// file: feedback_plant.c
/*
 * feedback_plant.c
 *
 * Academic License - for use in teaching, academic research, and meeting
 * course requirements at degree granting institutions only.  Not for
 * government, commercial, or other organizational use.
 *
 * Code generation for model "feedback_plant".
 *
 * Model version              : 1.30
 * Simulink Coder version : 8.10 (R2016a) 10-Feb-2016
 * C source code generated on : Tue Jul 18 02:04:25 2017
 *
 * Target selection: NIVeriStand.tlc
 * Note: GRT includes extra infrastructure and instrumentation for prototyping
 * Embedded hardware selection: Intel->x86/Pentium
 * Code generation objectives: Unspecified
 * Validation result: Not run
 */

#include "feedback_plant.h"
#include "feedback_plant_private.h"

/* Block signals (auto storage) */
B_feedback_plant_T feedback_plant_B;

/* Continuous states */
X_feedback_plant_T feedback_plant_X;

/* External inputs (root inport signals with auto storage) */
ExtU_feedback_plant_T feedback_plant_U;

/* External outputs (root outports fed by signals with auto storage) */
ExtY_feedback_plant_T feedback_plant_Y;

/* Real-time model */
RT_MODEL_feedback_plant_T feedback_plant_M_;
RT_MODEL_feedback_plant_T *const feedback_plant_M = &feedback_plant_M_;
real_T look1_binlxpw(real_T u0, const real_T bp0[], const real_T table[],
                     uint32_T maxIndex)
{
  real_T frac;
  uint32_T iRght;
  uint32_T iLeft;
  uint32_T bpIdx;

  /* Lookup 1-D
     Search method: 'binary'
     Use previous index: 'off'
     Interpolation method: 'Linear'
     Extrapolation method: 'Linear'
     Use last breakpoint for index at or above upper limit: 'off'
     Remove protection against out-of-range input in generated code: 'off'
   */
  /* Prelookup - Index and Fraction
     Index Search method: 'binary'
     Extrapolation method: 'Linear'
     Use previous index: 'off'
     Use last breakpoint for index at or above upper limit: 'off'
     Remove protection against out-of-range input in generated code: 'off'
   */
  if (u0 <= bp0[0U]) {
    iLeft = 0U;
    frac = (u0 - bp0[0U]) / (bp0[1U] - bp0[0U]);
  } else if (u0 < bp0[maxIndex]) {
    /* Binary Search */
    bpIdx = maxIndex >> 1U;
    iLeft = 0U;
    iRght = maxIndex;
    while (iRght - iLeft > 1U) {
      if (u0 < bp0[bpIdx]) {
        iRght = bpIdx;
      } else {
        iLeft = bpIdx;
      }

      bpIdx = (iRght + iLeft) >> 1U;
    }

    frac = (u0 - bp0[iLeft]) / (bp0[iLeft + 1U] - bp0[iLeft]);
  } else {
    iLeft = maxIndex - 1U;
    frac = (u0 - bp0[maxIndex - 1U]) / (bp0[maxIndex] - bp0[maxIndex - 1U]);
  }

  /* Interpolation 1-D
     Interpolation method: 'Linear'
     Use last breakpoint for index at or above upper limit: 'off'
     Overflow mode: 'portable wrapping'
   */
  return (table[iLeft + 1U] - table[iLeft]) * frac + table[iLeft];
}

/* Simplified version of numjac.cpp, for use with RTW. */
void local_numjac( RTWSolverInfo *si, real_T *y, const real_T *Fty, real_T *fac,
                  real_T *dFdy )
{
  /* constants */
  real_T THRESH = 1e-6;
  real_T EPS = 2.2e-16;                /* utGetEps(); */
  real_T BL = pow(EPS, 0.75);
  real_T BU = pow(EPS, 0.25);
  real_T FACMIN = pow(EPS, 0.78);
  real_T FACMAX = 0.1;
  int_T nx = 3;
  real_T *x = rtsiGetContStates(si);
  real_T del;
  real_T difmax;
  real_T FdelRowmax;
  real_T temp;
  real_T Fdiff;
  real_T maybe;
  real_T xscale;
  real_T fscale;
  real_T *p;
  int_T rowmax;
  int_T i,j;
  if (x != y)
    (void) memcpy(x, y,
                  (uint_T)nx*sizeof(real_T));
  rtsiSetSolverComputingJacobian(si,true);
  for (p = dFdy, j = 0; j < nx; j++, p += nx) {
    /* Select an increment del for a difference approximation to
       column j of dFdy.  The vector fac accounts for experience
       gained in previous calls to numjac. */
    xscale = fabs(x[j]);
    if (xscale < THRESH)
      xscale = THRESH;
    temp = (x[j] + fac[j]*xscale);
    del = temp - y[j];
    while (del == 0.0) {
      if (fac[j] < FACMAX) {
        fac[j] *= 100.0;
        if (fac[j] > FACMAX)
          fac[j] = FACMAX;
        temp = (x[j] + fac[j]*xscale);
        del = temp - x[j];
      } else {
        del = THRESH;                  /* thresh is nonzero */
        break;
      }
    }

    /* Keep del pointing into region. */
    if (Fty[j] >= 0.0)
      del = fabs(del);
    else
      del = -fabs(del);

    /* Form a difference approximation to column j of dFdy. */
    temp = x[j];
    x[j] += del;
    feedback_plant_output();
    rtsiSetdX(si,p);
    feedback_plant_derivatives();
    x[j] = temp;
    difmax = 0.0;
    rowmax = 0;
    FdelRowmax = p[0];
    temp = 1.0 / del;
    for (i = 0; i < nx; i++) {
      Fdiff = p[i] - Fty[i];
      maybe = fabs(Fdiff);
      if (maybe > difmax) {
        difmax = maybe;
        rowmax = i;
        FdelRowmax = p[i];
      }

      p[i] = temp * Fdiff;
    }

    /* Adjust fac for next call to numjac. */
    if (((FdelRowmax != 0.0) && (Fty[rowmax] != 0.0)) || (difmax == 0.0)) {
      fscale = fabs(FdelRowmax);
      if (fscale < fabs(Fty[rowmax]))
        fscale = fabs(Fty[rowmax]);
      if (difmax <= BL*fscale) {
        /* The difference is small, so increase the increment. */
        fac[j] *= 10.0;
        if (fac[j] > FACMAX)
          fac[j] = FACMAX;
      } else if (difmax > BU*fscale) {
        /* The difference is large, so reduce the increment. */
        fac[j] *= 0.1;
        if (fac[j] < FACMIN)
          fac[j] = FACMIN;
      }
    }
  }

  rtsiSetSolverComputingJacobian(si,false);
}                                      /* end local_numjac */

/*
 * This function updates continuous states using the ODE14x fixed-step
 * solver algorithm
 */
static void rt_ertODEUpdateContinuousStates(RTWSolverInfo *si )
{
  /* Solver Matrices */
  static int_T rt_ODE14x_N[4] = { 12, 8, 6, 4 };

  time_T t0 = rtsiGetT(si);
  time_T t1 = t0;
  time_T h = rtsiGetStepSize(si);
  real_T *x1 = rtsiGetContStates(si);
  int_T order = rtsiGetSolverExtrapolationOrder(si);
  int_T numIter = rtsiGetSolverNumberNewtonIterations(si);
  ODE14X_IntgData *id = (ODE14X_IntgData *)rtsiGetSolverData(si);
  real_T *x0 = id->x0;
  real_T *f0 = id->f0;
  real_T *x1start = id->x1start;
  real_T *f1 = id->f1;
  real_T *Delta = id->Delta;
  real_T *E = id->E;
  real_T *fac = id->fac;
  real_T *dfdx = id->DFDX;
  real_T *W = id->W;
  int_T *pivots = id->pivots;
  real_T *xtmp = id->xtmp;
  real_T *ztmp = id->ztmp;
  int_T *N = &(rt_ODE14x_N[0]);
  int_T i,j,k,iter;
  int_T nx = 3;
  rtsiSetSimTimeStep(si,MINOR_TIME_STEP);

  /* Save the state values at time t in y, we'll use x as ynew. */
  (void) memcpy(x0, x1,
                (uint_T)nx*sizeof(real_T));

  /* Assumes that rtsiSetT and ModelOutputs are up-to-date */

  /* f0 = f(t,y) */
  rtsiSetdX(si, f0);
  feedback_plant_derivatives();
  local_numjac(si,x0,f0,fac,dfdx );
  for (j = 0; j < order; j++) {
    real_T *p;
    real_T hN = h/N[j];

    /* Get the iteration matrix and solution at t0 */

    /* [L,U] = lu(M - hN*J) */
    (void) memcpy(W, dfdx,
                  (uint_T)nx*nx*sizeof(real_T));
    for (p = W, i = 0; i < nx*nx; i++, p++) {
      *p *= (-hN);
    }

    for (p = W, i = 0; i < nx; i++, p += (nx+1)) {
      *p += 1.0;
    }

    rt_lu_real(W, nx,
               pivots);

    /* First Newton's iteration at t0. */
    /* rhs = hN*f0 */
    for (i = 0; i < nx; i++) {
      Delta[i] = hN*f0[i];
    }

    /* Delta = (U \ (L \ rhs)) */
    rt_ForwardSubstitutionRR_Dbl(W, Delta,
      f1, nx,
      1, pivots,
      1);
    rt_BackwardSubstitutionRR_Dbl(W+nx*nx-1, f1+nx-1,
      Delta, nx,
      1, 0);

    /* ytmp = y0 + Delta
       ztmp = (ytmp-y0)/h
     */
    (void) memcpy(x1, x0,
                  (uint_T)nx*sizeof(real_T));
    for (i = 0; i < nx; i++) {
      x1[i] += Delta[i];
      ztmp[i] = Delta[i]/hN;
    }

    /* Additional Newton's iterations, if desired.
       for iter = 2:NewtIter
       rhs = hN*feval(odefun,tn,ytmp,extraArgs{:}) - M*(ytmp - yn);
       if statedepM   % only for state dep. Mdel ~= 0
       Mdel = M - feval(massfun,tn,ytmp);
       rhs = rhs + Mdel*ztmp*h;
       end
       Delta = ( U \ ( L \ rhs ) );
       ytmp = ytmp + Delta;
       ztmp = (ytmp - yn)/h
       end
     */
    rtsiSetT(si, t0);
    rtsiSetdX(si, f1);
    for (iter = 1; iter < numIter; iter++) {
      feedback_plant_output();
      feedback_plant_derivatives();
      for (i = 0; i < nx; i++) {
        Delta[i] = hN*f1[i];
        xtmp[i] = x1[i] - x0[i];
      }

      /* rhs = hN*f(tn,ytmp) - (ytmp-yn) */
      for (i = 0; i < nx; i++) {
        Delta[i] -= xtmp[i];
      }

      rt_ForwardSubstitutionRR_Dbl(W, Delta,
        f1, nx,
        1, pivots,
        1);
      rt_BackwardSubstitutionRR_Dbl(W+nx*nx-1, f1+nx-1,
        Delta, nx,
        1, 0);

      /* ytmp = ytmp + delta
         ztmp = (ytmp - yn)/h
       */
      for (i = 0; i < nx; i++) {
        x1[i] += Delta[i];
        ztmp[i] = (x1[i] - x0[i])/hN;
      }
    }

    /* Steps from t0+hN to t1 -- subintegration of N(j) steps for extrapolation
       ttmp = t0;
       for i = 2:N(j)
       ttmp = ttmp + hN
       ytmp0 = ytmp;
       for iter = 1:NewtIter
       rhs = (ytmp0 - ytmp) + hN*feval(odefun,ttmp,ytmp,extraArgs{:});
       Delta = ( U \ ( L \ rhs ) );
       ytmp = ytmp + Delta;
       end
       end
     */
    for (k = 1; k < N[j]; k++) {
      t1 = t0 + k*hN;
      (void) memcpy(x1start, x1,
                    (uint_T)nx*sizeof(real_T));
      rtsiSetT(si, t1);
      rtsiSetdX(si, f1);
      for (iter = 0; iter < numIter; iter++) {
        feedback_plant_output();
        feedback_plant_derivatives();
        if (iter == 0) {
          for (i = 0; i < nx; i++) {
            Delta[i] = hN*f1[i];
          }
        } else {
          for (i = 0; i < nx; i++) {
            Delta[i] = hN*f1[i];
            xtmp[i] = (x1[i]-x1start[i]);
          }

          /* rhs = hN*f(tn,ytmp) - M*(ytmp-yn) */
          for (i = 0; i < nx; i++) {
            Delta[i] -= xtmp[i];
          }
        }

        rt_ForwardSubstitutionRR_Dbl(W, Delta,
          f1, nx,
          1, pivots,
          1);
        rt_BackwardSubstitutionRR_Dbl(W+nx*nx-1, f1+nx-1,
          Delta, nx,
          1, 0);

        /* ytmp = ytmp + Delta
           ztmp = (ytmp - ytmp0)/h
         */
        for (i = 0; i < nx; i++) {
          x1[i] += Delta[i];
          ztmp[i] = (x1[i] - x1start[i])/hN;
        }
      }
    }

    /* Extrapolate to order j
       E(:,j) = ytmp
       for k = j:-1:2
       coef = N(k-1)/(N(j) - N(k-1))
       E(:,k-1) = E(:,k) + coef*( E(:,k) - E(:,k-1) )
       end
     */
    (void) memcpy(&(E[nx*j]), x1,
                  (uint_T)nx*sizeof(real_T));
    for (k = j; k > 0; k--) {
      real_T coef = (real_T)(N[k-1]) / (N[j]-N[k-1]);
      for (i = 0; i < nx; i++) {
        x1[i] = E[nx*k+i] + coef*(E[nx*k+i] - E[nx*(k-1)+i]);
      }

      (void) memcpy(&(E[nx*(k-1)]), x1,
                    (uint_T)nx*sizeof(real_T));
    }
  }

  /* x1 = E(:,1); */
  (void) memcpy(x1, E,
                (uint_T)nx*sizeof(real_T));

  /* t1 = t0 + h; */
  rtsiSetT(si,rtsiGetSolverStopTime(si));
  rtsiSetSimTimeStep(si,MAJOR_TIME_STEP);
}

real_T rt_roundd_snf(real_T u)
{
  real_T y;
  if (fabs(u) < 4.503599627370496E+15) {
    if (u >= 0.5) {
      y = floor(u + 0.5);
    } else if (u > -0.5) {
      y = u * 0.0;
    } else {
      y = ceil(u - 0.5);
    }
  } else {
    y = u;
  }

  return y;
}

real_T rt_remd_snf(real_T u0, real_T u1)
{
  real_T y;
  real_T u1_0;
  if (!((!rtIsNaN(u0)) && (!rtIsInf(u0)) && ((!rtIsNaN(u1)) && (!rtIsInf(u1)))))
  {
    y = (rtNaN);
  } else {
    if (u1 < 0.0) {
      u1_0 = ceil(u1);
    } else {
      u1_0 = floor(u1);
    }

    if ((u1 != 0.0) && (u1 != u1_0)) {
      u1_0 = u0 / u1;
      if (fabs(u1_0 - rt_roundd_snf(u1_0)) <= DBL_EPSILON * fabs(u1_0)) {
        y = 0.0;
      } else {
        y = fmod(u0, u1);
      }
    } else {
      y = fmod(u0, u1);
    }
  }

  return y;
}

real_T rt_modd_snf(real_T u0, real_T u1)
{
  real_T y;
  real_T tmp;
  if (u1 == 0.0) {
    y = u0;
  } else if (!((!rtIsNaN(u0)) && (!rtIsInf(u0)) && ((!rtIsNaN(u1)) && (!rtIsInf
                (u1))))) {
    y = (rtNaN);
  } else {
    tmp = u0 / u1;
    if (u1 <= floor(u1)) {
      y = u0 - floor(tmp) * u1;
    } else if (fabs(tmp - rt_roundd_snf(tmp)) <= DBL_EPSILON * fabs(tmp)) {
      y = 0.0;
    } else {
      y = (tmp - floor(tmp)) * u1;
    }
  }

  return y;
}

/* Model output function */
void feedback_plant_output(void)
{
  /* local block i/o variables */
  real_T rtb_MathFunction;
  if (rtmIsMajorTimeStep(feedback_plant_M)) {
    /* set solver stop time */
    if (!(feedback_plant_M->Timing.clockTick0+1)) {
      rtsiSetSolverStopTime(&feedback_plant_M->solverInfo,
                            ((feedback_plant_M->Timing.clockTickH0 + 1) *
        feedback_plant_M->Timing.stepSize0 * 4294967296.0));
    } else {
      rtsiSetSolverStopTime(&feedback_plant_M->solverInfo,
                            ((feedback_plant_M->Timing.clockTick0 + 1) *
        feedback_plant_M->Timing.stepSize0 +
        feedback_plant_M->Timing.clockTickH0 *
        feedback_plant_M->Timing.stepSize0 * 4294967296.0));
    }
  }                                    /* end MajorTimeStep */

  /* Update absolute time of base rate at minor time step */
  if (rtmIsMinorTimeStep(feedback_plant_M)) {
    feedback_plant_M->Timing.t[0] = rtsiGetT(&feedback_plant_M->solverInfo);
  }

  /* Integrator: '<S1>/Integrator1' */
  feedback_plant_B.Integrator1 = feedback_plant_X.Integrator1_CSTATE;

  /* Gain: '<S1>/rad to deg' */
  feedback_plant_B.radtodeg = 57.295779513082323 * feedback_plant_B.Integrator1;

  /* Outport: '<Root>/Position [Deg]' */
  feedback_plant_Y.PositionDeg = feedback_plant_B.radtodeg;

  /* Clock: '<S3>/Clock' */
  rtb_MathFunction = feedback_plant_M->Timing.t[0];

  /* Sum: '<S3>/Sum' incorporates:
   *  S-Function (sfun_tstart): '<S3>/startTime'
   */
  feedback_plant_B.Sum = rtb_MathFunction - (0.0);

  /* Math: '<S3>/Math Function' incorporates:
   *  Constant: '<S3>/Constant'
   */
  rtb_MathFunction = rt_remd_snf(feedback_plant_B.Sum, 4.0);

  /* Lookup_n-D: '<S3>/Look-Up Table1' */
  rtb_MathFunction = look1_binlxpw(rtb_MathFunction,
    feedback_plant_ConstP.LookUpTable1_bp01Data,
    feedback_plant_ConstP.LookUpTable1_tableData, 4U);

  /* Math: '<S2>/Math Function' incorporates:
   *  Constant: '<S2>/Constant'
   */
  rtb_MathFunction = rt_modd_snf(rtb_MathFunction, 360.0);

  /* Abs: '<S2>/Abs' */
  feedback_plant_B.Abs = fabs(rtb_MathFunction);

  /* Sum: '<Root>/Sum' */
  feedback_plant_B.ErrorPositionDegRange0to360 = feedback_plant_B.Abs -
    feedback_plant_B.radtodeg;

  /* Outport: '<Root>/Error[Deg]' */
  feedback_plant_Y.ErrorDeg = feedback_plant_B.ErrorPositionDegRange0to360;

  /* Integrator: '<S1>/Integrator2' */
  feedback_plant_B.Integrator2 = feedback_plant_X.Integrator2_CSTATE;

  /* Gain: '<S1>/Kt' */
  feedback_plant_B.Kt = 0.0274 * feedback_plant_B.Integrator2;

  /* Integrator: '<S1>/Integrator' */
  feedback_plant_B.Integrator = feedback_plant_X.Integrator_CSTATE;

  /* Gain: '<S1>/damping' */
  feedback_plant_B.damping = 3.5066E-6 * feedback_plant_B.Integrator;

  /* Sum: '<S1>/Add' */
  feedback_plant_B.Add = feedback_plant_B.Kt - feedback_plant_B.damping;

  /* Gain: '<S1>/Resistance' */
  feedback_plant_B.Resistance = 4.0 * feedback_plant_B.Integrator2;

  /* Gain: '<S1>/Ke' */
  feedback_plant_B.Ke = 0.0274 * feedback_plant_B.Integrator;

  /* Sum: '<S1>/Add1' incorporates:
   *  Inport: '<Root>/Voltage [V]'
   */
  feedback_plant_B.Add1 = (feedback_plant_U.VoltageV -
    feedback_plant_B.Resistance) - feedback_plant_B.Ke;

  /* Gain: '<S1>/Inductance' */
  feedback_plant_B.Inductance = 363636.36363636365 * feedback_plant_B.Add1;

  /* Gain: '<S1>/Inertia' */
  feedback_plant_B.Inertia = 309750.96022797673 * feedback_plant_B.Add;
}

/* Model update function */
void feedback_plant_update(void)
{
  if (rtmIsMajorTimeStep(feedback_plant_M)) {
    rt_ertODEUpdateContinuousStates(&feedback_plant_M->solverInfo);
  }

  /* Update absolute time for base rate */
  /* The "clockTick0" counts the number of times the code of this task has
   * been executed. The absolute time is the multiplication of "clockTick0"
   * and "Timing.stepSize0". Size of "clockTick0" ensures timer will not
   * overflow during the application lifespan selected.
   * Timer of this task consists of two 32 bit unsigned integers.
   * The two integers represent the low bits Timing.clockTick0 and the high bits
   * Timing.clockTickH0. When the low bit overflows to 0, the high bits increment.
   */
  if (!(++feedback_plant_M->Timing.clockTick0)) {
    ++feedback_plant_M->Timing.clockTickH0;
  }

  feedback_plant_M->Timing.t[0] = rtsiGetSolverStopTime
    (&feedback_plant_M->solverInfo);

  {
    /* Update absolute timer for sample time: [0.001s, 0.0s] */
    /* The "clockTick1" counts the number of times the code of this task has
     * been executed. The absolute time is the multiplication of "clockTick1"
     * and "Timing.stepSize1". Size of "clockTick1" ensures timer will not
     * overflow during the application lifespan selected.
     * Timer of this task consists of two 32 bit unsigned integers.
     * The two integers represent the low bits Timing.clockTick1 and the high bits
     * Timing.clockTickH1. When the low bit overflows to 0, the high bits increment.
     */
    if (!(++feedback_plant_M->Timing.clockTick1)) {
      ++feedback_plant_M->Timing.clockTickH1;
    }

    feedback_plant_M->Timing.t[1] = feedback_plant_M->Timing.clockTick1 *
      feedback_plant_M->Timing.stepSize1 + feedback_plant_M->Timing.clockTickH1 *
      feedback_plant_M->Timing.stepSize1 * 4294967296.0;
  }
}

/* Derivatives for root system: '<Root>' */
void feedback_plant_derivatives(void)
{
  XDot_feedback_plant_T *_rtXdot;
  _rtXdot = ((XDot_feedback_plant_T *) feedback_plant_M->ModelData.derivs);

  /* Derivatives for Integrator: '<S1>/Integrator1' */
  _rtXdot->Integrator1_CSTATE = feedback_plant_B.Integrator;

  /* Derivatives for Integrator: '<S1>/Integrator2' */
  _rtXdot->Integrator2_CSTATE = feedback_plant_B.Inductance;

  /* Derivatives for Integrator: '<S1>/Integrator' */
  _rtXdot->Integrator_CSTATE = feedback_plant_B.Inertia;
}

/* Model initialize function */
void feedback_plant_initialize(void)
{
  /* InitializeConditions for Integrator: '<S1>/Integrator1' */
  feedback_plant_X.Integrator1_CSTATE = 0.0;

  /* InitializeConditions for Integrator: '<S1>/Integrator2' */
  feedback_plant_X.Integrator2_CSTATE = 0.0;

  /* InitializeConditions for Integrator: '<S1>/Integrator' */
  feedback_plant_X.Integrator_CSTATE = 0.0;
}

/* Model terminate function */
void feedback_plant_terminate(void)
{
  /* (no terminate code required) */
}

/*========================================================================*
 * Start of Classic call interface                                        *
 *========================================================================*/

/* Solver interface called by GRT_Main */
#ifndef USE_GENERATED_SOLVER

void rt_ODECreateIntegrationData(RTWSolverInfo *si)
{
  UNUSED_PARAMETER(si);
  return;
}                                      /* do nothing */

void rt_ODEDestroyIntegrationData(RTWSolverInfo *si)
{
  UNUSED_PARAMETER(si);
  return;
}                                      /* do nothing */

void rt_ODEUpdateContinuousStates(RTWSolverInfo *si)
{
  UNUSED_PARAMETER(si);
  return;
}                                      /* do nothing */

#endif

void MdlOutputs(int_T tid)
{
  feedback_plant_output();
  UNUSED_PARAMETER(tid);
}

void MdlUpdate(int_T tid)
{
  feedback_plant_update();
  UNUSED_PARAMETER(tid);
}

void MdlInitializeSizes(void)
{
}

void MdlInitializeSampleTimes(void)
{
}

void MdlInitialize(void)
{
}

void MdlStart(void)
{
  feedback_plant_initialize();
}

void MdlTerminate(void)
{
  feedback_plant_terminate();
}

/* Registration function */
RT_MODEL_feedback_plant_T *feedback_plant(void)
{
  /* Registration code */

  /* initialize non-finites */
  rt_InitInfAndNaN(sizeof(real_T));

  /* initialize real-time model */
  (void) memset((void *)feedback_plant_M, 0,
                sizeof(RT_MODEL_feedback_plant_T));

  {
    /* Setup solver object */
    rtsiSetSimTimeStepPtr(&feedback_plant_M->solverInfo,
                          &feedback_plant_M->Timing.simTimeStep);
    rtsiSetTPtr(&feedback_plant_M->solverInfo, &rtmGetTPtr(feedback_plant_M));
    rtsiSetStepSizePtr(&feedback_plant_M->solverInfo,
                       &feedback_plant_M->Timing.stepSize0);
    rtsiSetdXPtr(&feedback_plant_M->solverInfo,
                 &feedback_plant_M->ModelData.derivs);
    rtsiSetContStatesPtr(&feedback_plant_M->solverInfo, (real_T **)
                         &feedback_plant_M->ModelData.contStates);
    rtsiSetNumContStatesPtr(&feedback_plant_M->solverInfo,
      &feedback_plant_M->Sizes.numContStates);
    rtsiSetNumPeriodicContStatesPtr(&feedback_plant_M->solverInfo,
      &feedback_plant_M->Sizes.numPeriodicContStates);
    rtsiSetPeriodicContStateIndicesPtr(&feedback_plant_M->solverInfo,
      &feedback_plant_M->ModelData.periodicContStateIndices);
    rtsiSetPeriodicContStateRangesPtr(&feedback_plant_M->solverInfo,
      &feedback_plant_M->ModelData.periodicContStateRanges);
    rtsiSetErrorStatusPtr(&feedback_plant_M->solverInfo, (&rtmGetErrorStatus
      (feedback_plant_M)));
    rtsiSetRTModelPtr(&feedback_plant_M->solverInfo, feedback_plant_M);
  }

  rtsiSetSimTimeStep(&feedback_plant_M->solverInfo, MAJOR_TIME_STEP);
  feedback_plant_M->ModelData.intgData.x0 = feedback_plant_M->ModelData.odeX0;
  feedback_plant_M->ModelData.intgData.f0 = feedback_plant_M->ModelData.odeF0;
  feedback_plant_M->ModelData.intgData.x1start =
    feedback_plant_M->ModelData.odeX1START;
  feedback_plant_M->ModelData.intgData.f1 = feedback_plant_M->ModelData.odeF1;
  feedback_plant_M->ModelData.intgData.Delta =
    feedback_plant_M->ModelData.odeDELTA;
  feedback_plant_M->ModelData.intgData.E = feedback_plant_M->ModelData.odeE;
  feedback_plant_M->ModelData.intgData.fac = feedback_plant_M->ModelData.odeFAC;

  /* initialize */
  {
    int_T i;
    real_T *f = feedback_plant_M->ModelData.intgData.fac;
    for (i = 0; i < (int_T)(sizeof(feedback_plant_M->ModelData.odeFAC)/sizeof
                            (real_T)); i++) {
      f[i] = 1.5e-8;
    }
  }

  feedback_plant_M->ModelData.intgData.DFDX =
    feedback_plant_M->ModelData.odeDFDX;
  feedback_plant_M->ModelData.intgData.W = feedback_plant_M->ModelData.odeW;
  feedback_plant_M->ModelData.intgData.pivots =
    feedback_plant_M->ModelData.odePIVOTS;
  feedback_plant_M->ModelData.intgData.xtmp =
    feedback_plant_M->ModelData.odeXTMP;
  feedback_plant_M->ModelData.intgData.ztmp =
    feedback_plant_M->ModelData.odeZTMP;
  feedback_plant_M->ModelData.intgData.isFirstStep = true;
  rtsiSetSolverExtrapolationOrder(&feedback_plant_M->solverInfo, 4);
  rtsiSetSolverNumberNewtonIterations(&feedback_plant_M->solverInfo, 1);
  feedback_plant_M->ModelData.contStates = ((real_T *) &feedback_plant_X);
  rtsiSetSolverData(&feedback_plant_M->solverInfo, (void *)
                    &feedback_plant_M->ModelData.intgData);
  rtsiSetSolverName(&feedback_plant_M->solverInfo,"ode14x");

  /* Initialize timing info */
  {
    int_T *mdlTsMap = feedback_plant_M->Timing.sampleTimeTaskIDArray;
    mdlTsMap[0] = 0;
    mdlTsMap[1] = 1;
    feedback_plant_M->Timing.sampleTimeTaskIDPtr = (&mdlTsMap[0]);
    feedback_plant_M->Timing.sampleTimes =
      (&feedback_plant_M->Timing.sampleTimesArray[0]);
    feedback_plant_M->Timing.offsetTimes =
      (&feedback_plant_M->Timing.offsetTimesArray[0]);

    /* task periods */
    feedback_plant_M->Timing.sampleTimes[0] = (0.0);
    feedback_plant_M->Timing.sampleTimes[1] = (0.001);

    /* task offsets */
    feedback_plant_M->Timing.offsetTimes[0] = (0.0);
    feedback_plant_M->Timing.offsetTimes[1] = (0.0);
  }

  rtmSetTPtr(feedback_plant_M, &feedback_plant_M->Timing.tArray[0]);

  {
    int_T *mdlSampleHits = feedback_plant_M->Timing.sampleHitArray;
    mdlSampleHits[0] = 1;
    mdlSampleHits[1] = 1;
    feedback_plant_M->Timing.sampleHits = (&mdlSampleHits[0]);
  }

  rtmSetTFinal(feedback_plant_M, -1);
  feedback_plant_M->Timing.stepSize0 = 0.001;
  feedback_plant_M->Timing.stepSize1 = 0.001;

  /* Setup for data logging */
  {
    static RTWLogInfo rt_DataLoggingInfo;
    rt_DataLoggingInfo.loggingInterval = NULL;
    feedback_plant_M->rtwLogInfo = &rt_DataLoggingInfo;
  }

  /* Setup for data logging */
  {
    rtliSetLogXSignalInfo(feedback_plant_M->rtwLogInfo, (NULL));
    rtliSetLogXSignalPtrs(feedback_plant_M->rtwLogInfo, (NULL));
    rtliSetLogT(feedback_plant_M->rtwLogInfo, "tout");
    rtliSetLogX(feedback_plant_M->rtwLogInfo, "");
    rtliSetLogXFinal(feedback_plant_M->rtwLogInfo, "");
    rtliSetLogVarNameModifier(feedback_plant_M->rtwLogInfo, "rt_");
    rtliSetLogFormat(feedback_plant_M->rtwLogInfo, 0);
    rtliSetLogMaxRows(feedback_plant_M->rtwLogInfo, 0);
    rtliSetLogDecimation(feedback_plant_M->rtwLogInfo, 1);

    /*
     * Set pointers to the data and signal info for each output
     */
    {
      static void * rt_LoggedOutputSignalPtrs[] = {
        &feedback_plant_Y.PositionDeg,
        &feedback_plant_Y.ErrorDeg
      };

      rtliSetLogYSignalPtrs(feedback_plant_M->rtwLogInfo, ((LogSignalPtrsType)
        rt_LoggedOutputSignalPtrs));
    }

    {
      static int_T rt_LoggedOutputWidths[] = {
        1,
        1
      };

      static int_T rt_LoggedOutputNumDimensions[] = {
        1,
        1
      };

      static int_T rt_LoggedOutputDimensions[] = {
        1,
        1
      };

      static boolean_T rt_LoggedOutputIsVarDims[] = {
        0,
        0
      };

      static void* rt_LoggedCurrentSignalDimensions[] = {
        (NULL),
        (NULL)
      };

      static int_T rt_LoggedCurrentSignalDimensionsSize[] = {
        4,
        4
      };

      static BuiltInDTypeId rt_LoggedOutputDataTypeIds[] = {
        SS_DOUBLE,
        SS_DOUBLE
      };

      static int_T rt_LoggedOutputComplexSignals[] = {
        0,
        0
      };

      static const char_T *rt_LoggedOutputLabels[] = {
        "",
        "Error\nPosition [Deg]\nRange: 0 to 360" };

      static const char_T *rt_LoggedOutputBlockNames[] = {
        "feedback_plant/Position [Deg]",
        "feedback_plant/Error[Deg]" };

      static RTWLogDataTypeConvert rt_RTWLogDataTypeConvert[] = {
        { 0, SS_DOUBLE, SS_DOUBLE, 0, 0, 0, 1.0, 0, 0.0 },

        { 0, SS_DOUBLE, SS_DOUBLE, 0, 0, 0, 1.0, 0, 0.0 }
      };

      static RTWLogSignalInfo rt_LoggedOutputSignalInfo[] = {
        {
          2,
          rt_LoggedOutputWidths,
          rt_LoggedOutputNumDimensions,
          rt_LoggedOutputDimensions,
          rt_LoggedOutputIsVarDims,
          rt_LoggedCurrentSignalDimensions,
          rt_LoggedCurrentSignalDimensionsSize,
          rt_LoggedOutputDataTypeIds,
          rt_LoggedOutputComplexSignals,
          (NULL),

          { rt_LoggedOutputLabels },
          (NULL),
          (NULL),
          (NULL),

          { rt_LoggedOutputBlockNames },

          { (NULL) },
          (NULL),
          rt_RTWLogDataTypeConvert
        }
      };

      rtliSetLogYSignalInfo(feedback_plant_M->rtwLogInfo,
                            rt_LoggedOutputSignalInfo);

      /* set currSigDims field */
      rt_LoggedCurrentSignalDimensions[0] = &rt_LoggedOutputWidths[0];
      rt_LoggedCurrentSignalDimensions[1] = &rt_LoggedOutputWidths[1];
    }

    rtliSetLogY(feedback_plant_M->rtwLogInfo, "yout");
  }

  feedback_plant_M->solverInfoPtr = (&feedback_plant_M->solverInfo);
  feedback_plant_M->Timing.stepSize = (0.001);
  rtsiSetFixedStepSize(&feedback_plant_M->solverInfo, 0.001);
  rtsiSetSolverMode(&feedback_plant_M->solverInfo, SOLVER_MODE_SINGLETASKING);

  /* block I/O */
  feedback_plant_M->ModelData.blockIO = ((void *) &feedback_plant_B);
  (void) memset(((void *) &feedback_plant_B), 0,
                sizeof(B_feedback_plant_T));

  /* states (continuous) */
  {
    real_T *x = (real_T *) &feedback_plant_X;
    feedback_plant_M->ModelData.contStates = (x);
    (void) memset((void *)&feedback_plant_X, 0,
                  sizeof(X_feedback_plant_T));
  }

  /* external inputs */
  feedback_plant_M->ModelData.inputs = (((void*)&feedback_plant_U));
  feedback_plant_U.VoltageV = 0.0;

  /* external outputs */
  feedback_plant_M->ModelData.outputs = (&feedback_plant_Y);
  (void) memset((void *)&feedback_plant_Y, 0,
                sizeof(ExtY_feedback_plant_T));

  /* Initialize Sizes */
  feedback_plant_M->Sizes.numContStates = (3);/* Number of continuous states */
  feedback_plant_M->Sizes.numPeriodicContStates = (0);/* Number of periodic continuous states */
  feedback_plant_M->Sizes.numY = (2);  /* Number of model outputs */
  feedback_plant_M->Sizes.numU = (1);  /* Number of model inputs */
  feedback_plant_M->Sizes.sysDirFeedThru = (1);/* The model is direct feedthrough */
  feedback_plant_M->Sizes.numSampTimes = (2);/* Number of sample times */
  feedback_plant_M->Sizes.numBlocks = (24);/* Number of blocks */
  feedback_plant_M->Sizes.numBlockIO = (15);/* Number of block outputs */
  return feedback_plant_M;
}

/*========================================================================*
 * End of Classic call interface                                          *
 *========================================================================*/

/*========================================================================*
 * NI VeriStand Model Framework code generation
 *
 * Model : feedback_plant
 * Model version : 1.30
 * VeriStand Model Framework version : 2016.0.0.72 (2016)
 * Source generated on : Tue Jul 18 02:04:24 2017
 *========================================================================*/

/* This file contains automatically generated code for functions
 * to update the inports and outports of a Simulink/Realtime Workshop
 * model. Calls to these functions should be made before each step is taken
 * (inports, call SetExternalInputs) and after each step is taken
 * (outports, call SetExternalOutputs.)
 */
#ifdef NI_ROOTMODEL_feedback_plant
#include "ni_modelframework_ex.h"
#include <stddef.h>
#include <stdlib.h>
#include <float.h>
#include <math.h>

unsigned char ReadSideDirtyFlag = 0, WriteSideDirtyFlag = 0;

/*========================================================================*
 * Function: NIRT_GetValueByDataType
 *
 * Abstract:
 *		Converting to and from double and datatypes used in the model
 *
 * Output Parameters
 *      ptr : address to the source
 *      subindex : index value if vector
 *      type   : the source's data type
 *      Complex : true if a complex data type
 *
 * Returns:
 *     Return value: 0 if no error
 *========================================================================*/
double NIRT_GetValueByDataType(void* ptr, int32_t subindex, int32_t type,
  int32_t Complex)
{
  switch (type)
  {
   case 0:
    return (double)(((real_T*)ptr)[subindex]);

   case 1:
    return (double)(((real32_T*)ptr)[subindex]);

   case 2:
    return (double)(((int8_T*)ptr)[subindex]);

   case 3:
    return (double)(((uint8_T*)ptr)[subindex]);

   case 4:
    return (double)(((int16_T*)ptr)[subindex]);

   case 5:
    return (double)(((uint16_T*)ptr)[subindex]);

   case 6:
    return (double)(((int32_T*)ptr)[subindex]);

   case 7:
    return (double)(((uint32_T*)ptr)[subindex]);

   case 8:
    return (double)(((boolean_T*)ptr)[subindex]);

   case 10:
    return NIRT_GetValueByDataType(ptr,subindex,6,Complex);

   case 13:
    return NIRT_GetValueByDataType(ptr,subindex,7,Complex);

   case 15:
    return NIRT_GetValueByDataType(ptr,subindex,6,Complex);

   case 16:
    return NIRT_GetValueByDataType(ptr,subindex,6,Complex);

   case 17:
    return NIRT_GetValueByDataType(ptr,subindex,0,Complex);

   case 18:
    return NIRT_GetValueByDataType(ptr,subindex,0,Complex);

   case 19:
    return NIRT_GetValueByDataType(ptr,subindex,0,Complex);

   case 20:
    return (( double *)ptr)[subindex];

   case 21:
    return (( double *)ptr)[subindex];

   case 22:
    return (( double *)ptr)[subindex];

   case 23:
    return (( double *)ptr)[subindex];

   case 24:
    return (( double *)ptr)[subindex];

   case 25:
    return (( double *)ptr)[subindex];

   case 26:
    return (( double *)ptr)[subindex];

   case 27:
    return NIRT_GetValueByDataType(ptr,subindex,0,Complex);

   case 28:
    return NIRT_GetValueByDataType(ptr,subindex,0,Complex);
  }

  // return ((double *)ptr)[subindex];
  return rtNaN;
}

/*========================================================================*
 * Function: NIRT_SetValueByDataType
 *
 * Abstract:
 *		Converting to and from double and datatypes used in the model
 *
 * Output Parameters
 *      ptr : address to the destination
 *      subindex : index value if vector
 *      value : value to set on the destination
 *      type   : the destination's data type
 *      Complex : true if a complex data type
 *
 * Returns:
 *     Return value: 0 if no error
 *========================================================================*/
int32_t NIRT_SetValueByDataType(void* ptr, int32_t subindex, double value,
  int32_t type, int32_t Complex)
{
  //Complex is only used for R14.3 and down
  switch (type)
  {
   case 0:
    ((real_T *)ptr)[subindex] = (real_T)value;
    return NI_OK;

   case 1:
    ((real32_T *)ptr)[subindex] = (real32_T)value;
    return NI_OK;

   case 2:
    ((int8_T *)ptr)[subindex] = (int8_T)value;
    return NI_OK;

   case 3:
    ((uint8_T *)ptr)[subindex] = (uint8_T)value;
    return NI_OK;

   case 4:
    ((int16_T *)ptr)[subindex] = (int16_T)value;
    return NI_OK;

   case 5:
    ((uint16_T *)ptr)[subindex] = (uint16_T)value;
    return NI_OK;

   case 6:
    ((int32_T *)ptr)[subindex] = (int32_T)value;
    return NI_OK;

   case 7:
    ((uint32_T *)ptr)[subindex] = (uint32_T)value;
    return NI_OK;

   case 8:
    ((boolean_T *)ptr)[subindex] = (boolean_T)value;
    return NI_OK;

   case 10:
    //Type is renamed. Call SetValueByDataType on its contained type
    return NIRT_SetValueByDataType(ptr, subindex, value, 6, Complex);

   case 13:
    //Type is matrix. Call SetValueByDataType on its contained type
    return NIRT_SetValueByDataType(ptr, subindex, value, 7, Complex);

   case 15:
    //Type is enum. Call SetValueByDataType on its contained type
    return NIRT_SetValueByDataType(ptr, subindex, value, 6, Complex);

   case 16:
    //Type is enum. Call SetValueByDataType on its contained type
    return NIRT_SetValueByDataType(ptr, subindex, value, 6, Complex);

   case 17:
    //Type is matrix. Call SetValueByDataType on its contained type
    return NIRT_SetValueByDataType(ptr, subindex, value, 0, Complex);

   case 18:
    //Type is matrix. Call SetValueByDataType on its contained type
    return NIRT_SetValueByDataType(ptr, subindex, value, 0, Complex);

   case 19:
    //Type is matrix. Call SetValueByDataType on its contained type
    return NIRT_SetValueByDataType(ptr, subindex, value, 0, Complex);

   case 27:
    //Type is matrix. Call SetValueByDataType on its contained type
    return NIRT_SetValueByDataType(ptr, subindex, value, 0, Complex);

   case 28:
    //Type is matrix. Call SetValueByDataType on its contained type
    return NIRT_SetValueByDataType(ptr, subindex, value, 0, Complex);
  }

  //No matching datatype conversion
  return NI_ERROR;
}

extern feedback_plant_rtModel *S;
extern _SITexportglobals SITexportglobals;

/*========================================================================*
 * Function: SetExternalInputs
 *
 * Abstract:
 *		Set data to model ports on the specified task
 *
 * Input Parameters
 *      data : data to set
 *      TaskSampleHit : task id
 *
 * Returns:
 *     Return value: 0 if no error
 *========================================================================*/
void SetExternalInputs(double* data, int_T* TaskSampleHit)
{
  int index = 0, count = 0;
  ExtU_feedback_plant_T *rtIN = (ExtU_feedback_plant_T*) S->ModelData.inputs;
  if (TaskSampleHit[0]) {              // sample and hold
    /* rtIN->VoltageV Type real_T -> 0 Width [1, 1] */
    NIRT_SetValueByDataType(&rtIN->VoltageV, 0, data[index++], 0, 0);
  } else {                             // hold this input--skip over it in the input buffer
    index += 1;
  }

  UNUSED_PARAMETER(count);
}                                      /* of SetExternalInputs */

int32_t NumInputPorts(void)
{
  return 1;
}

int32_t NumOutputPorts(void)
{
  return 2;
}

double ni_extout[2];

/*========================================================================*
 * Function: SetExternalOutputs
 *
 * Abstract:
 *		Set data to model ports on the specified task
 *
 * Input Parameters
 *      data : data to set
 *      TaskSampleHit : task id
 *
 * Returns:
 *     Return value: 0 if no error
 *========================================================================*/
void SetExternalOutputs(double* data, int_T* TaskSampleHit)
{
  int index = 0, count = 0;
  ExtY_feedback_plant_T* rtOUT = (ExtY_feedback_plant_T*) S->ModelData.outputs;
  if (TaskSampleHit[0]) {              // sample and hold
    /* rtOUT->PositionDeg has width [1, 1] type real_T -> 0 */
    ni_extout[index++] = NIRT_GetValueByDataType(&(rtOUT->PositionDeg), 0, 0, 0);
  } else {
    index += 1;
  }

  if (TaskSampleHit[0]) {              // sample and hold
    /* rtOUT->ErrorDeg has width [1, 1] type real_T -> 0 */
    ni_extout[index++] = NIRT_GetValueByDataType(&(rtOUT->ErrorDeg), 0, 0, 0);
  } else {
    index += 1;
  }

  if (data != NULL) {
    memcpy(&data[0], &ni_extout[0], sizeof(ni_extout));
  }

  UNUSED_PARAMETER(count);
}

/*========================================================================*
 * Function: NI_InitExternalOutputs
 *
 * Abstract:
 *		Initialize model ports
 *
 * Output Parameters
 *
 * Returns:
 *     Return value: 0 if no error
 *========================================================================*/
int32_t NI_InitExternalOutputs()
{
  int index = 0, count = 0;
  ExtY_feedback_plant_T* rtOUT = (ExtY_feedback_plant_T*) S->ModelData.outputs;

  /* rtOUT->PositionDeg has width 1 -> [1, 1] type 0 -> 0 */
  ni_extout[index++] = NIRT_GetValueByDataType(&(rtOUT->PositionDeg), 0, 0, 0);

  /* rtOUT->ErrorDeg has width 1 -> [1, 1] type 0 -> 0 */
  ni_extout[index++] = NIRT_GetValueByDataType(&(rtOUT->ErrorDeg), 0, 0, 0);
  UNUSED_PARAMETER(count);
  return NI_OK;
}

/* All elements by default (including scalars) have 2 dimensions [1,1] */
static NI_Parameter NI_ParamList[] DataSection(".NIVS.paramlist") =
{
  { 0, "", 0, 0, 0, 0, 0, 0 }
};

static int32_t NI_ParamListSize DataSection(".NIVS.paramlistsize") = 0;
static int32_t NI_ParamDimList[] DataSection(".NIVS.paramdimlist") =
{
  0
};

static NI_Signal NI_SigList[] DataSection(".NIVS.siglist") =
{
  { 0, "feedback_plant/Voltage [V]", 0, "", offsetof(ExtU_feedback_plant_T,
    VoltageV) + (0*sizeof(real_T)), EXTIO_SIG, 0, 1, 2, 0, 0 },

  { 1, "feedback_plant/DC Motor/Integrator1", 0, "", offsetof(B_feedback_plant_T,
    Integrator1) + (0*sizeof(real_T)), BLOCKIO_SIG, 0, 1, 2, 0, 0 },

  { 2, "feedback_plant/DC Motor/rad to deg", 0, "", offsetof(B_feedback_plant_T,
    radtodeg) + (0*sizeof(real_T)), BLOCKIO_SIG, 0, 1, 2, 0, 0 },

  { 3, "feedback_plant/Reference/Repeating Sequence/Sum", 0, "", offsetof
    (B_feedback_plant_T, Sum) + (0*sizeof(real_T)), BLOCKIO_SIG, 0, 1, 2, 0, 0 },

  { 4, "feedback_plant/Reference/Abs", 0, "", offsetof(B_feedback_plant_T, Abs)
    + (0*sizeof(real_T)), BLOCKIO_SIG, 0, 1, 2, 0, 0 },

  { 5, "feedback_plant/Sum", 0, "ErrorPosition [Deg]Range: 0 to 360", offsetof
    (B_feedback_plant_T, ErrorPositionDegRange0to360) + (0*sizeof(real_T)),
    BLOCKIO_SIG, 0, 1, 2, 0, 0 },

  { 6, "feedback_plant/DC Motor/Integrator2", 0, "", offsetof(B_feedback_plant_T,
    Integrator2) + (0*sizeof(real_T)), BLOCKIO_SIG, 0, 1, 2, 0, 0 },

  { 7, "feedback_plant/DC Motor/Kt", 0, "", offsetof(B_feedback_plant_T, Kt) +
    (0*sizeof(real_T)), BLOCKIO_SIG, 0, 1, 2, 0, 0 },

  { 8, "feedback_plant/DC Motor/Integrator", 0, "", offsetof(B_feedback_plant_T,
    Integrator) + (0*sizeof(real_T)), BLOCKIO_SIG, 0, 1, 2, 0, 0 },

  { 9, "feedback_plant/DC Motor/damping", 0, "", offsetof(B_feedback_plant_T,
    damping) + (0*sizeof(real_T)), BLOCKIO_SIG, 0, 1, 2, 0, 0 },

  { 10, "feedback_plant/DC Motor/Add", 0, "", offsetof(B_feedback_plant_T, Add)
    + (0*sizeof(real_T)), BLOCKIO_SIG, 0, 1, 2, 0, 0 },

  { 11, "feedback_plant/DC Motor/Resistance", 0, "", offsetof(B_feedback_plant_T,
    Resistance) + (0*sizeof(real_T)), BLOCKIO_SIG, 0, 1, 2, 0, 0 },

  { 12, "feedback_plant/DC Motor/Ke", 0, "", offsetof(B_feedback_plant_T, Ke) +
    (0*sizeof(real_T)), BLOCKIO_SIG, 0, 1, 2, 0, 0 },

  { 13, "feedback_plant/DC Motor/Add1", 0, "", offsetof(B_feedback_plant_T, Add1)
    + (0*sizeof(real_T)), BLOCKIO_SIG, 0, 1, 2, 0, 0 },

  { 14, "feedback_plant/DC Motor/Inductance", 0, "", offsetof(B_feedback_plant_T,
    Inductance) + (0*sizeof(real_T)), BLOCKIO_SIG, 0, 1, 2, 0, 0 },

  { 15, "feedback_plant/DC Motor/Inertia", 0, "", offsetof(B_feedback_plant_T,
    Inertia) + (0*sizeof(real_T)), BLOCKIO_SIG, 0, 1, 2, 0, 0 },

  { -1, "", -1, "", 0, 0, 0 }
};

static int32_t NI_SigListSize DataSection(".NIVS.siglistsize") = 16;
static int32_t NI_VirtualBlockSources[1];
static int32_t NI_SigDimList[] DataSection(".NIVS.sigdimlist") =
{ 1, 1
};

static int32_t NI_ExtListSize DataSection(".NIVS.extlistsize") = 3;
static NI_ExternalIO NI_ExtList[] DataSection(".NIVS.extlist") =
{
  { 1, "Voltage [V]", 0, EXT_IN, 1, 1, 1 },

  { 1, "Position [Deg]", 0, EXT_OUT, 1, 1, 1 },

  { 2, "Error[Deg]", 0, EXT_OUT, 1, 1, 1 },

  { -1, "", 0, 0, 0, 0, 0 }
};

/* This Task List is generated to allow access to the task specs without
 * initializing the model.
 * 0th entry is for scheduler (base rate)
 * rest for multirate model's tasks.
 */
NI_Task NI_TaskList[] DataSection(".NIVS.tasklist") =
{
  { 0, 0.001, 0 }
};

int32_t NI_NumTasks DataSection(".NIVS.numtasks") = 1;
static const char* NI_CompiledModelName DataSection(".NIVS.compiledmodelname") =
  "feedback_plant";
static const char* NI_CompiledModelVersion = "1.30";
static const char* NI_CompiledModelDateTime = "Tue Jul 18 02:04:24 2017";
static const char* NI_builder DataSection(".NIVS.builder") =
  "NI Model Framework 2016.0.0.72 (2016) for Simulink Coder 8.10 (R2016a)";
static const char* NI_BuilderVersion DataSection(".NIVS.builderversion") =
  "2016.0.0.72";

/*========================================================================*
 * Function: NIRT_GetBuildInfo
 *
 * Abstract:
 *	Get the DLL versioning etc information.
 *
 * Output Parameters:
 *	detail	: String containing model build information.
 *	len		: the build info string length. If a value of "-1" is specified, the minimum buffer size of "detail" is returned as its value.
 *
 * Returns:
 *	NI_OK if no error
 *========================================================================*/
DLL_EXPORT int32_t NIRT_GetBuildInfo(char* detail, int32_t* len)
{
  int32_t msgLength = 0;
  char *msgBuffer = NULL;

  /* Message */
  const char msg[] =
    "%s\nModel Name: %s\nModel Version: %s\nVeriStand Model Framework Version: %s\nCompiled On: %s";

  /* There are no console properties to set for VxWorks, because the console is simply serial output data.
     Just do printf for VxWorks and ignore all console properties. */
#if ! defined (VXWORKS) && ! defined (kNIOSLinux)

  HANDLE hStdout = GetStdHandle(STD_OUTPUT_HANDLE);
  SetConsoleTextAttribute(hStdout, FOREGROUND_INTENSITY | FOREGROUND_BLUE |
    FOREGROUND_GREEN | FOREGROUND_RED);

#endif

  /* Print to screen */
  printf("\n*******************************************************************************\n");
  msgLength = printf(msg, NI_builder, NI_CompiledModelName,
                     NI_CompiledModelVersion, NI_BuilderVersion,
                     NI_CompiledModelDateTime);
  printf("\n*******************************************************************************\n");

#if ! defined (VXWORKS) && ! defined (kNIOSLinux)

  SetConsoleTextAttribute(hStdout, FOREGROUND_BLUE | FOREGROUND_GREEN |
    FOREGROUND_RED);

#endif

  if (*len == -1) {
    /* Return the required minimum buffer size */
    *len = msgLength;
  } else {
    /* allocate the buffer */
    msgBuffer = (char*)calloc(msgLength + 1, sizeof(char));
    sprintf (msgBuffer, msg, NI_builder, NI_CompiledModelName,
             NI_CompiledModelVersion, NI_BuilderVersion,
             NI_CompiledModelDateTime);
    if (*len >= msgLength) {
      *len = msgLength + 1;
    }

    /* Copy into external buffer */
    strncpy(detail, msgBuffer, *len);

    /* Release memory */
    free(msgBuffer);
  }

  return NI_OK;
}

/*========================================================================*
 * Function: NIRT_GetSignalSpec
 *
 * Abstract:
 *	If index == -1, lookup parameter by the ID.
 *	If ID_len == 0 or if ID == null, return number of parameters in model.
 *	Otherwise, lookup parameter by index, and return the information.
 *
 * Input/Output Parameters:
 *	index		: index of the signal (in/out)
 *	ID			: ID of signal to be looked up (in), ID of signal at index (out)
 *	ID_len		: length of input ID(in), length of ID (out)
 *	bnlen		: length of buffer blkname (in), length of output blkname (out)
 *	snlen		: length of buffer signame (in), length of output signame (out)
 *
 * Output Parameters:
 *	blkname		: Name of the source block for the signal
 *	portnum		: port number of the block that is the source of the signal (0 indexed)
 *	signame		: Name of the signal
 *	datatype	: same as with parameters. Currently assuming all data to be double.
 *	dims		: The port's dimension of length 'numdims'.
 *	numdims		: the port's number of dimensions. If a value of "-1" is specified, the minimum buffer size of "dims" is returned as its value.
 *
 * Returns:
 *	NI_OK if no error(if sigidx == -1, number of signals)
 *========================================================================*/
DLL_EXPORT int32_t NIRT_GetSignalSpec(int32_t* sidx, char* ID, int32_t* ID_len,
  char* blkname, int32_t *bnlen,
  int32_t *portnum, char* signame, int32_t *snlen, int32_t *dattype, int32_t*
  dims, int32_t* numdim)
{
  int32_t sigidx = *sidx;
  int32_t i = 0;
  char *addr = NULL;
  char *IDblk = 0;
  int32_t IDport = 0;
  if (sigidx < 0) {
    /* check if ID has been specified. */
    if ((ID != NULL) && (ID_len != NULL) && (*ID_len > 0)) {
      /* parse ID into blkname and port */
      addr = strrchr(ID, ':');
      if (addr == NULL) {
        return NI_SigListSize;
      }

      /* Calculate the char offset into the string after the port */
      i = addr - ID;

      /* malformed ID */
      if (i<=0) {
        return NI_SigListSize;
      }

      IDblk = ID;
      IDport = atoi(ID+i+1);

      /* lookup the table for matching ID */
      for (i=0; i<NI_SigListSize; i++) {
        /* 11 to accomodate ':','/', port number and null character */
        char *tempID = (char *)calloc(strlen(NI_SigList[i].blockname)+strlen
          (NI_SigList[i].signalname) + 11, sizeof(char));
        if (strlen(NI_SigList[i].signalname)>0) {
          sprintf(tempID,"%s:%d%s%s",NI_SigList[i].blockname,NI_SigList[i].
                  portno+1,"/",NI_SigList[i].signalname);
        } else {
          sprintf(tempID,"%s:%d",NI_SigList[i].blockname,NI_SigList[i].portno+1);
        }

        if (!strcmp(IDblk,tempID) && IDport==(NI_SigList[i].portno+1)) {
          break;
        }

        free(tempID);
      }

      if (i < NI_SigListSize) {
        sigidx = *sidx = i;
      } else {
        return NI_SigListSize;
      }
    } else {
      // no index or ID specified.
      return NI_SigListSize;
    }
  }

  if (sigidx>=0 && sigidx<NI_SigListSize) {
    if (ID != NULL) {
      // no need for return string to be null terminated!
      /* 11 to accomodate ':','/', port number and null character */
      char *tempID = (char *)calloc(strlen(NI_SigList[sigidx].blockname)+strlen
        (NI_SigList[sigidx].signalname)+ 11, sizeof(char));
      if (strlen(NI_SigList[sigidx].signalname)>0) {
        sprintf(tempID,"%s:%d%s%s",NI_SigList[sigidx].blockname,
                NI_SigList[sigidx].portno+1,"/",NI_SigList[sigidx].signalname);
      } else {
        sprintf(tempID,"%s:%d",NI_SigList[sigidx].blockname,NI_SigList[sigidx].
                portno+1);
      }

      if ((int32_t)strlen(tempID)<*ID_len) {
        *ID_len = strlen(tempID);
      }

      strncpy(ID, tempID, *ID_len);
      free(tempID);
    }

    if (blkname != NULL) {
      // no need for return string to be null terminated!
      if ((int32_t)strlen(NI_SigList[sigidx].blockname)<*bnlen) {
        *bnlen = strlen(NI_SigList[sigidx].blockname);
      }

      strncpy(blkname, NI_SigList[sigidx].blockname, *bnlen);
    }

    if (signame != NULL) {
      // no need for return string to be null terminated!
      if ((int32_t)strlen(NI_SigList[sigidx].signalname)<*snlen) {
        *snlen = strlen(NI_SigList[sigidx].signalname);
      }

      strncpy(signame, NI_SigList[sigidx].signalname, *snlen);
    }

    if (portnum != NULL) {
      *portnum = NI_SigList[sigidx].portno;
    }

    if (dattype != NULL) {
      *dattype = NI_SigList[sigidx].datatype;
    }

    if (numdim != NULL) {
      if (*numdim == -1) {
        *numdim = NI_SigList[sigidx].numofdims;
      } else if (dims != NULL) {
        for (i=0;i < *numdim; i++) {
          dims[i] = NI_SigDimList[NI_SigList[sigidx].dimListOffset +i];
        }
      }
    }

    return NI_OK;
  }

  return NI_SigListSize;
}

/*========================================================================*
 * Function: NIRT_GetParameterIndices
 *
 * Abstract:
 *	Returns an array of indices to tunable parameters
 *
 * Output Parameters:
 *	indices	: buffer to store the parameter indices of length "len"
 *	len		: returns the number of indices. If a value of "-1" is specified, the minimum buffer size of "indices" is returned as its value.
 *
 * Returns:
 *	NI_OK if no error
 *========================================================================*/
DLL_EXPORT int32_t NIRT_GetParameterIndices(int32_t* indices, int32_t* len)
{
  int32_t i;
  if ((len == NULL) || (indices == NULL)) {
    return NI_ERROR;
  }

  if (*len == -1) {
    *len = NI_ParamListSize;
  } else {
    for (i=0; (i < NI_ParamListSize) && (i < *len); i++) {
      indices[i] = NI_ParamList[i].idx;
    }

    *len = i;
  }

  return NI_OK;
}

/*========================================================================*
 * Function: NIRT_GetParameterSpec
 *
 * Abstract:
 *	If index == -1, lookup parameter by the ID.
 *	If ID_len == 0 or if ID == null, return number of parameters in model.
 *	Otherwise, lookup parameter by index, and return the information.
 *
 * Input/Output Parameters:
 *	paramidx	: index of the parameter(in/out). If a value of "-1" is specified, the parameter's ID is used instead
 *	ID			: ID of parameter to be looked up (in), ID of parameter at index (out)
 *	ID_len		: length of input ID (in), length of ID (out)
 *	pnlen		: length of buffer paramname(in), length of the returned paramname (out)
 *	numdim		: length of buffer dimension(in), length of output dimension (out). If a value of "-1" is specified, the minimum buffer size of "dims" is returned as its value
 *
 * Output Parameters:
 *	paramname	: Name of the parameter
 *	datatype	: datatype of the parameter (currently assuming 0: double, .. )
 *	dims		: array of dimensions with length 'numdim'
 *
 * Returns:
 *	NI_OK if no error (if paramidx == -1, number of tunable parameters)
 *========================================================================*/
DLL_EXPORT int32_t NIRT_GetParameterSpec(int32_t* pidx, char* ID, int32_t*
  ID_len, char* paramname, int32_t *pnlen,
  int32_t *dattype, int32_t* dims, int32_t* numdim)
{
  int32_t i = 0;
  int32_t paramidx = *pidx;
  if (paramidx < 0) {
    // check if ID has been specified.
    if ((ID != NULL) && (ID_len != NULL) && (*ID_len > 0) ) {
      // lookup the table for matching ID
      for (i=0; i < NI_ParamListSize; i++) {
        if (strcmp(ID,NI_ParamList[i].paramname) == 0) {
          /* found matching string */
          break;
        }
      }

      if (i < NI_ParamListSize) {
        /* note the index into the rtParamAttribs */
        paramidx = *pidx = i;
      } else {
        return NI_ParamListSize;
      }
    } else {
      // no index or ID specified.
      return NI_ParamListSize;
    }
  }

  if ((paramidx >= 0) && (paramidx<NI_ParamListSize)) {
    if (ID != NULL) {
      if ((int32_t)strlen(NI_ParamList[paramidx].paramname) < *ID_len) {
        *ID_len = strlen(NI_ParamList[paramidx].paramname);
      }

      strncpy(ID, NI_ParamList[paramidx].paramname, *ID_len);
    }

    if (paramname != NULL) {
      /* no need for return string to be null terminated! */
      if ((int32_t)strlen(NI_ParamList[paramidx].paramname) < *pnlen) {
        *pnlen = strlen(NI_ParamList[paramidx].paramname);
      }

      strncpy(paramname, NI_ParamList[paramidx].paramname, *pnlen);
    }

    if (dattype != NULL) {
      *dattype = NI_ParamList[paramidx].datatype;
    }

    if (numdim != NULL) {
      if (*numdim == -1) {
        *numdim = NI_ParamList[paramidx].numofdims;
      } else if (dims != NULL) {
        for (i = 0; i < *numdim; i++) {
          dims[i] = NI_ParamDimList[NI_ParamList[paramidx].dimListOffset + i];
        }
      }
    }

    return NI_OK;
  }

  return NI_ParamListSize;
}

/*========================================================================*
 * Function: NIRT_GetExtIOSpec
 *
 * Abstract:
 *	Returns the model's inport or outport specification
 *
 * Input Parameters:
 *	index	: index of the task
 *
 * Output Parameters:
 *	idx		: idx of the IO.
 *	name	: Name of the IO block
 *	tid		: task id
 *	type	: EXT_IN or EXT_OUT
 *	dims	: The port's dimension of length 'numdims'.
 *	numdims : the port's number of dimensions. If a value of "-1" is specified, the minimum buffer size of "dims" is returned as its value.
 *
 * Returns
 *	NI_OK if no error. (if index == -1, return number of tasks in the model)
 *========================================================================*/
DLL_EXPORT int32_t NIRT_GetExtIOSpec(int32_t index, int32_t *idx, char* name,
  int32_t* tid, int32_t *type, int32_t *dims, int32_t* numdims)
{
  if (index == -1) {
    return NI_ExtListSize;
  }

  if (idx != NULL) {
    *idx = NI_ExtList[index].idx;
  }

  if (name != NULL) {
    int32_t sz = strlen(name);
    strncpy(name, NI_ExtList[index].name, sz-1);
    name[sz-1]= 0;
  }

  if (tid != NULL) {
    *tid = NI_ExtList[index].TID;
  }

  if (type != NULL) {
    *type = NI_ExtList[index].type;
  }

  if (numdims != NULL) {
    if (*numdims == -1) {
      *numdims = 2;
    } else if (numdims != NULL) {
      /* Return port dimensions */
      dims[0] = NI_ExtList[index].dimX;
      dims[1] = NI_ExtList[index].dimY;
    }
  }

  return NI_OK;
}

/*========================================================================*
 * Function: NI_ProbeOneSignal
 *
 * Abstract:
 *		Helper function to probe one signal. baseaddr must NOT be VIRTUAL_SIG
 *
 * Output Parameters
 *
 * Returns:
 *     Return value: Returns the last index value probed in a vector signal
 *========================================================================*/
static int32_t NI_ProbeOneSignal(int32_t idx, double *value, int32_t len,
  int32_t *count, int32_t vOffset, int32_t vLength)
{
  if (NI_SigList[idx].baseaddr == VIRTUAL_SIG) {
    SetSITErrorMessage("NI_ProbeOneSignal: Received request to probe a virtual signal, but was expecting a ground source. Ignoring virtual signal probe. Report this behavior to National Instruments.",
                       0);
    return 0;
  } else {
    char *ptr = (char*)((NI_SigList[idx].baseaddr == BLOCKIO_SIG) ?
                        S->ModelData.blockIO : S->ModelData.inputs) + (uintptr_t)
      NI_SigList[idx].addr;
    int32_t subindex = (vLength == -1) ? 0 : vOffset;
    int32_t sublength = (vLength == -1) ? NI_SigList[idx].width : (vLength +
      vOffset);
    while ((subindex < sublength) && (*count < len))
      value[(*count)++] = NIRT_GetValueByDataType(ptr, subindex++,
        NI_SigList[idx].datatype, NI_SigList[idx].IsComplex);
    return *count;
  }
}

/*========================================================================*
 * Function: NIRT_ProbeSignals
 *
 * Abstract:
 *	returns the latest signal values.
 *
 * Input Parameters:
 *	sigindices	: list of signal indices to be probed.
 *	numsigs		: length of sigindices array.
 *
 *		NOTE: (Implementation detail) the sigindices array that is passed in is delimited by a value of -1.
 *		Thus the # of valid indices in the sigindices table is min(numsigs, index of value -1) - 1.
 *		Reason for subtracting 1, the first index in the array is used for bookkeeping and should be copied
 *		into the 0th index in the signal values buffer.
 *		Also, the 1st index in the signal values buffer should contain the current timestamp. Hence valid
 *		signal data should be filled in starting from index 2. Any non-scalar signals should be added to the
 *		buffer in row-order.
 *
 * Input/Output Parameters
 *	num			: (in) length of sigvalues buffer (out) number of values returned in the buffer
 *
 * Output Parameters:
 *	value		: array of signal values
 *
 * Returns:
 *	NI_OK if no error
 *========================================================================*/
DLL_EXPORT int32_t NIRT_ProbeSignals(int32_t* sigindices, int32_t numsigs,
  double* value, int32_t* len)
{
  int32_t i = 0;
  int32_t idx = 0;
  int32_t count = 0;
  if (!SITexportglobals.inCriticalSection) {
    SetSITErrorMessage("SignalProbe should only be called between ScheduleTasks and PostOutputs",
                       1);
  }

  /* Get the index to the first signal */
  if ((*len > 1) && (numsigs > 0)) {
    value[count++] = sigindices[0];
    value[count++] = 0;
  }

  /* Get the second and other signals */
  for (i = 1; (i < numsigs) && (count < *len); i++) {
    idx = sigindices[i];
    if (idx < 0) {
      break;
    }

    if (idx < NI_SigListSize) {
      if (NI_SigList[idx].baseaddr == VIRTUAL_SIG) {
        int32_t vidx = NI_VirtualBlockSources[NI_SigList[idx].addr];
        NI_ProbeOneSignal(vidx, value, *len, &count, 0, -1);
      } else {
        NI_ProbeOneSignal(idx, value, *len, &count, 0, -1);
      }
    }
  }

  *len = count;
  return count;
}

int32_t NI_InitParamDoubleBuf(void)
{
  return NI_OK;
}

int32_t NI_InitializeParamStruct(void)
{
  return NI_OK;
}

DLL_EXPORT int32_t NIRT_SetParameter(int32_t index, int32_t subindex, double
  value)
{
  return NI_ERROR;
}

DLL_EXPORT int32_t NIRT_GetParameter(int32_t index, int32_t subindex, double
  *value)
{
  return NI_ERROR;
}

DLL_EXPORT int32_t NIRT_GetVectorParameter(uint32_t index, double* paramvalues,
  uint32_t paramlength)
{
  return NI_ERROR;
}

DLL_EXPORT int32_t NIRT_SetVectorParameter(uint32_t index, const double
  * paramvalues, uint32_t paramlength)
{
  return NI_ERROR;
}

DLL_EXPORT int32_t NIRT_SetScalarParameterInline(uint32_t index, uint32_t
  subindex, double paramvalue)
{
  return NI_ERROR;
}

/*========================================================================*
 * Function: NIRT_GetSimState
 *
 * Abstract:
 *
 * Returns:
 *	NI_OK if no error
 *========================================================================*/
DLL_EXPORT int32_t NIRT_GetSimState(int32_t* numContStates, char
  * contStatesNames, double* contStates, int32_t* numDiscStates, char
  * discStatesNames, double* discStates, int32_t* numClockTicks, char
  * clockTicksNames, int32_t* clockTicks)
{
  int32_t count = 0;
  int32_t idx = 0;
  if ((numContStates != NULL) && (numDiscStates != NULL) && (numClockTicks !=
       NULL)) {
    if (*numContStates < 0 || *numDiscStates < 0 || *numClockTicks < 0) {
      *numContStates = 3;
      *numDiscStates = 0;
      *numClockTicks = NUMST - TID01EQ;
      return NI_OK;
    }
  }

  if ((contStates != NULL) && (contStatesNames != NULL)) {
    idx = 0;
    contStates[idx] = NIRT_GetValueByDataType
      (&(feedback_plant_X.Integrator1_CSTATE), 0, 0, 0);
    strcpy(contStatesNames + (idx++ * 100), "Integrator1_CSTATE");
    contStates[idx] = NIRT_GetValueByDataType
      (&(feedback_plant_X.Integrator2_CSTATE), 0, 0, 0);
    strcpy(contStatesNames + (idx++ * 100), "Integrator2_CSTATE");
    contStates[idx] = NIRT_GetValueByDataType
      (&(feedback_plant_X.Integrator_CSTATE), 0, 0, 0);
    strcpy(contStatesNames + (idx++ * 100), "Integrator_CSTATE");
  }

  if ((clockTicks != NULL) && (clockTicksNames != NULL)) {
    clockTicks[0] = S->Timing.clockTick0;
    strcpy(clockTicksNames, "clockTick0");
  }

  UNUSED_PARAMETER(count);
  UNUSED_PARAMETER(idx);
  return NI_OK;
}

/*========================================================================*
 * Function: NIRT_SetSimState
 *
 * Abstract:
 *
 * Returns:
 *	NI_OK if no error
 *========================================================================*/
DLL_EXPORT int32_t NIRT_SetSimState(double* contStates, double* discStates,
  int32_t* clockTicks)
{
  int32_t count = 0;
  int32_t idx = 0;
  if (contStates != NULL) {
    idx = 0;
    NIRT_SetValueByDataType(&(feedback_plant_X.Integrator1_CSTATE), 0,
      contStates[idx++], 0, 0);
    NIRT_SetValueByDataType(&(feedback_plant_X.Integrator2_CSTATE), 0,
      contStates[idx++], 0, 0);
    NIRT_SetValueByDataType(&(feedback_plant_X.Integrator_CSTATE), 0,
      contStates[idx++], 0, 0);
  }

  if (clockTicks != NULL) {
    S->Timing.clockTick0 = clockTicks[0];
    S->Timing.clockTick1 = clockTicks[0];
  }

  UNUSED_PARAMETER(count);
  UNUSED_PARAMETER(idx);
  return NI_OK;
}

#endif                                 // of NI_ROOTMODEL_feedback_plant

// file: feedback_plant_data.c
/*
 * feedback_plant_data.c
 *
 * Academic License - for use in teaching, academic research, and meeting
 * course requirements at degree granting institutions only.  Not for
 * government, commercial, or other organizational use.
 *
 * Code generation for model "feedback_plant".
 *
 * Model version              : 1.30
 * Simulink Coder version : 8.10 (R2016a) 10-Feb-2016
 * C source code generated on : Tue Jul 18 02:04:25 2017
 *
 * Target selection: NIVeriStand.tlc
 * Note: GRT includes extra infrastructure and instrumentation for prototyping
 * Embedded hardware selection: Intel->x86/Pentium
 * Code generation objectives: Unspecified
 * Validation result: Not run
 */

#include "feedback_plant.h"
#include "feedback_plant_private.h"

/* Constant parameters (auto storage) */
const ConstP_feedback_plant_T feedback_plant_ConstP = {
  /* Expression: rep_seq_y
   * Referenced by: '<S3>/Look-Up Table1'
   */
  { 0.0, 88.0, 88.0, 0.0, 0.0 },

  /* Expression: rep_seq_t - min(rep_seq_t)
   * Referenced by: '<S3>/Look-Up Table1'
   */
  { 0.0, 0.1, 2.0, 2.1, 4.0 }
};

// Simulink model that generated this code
simulink model "feedback_plant"  (R2016a)
settings: Solver=ode14x  StartTime=0.0  StopTime=inf  FixedStep=1e-3  MaxStep=0.1  RelTol=1e-3
undefined symbols (not defined in the file): b, J, K, L, R
libraries: simulink x1

== system feedback_plant ==
  note: Reference
      | Position [Deg]
      | Range: 0 to 360
  note: Copyright 2012-2015 The MathWorks, Inc.
  note: DC Motor
      | The model simulates a DC motor, receiving as input the control voltage, and producing the position in degree of the DC motor shaft.
  Voltage [V] : Inport
  DC Motor : Subsystem
  Reference : Subsystem
  Sum : Sum  Inputs=|+-
  Position [Deg] : Outport
  Error[Deg] : Outport  Port=2
  wires:
  Voltage [V]/1 -> DC Motor/1(Voltage)
  Reference/1(Ref [Deg]) -> Sum/1
  Sum/1 -> Error[Deg]/1  "Error Position [Deg] Range: 0 to 360"
  DC Motor/1(Position) -> Sum/2, Position [Deg]/1

== system feedback_plant/DC Motor ==
  note: i
  note: d/dt(theta)
  note: d2/dt2(theta)
  note: d/dt(i)
  note: theta
  Voltage : Inport
  Add : Sum  Inputs=+-
  Add1 : Sum  Inputs=-+-
  Inductance : Gain  Gain=1/L
  Inertia : Gain  Gain=1/J
  Integrator : Integrator
  Integrator1 : Integrator
  Integrator2 : Integrator
  Ke : Gain  Gain=K
  Kt : Gain  Gain=K
  Resistance : Gain  Gain=R
  damping : Gain  Gain=b
  rad to deg : Gain  Gain=180/pi
  Position : Outport
  wires:
  Inductance/1 -> Integrator2/1
  Integrator/1 -> Integrator1/1, damping/1, Ke/1
  Integrator1/1 -> rad to deg/1
  Inertia/1 -> Integrator/1
  Integrator2/1 -> Kt/1, Resistance/1
  Add/1 -> Inertia/1
  Add1/1 -> Inductance/1
  Kt/1 -> Add/1
  damping/1 -> Add/2
  Ke/1 -> Add1/3
  Resistance/1 -> Add1/1
  Voltage/1 -> Add1/2
  rad to deg/1 -> Position/1

== system feedback_plant/Reference ==
  note: Reference input model
      | Provide the reference for the DC motor shaft (in degree) to be followed by the controller.
  Abs : Abs
  Constant : Constant  Value=360
  Math Function : Math  Operator=mod  SaturateOnIntegerOverflow=on
  Repeating Sequence : simulink/Sources/Repeating Sequence  rep_seq_t=[0 0.1 2 2.1 4]  rep_seq_y=[0 88 88 0 0].'
  Ref [Deg] : Outport
  wires:
  Constant/1 -> Math Function/2
  Repeating Sequence/1 -> Math Function/1
  Math Function/1 -> Abs/1
  Abs/1 -> Ref [Deg]/1
